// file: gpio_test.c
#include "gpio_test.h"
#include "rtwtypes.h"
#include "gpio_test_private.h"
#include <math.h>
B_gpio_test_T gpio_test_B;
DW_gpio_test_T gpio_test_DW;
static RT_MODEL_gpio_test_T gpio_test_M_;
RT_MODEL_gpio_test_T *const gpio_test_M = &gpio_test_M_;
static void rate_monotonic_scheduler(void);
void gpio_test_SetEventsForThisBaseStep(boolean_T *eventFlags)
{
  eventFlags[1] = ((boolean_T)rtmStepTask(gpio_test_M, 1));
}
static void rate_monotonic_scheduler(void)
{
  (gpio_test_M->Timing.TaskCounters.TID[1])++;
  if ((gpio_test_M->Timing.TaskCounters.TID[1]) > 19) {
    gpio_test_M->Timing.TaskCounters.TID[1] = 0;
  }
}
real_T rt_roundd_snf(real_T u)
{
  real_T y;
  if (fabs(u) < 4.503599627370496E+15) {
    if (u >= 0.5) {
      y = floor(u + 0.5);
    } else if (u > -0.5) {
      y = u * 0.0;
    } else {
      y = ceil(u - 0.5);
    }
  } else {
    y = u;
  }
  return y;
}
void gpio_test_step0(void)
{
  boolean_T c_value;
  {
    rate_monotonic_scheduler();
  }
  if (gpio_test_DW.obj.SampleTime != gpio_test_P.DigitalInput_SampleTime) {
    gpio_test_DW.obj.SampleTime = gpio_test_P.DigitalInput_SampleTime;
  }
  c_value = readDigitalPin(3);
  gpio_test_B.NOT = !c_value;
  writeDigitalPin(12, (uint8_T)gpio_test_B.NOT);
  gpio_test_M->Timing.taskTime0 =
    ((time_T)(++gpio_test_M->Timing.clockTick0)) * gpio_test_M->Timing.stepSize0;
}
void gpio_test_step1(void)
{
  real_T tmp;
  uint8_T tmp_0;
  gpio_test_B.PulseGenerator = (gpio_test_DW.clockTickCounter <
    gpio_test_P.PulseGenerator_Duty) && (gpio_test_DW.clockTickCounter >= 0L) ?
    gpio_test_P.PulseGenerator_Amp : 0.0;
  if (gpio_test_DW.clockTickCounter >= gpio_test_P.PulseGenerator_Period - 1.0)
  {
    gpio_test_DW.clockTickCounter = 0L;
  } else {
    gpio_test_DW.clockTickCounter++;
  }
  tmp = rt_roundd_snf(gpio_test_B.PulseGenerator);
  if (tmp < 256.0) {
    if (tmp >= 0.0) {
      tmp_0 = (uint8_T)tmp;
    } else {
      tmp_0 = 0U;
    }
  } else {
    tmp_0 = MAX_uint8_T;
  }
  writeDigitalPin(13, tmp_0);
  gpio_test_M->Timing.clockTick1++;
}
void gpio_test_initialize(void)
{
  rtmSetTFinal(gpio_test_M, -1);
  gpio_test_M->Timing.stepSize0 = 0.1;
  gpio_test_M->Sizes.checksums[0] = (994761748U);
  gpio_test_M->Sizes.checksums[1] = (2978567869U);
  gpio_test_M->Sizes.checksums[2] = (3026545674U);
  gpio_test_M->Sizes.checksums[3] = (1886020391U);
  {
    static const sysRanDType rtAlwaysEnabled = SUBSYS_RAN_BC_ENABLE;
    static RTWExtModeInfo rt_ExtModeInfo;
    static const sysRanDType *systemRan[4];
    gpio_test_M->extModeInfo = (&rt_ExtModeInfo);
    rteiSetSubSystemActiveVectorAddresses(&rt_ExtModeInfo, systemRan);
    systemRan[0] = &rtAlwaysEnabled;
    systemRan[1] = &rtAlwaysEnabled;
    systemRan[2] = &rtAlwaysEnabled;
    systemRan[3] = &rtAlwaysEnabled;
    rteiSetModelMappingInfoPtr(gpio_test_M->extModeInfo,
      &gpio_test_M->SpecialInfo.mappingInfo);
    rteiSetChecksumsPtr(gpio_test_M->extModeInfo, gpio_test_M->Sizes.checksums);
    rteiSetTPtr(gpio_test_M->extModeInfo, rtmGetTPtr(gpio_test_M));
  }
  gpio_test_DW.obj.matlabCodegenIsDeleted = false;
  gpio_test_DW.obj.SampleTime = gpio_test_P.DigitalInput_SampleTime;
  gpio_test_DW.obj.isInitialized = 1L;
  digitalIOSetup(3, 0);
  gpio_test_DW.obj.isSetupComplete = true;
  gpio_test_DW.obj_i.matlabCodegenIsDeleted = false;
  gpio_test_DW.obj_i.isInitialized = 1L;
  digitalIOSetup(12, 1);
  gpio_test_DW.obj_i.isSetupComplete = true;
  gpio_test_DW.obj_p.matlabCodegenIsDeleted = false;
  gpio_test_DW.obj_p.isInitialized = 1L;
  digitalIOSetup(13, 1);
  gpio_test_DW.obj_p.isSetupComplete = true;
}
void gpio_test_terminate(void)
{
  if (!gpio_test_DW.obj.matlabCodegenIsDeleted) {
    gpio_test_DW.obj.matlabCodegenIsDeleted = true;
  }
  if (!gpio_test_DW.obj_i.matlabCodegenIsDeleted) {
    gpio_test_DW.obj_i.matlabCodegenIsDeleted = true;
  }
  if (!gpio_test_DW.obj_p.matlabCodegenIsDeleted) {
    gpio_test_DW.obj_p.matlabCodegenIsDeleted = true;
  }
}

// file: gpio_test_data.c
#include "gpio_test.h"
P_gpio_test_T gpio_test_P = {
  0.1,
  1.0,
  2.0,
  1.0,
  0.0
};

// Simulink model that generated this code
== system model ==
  DigitalOutput#1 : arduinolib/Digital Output  pinNumber=12  <- 1: NOT
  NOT : Logic  Operator=NOT  <- 1: DigitalInput
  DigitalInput : arduinolib/Digital Input  pinNumber=3
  DigitalOutput#2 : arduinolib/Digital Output  pinNumber=13  <- 1: PulseGenerator
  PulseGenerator : DiscretePulseGenerator  Period=4  PulseWidth=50
